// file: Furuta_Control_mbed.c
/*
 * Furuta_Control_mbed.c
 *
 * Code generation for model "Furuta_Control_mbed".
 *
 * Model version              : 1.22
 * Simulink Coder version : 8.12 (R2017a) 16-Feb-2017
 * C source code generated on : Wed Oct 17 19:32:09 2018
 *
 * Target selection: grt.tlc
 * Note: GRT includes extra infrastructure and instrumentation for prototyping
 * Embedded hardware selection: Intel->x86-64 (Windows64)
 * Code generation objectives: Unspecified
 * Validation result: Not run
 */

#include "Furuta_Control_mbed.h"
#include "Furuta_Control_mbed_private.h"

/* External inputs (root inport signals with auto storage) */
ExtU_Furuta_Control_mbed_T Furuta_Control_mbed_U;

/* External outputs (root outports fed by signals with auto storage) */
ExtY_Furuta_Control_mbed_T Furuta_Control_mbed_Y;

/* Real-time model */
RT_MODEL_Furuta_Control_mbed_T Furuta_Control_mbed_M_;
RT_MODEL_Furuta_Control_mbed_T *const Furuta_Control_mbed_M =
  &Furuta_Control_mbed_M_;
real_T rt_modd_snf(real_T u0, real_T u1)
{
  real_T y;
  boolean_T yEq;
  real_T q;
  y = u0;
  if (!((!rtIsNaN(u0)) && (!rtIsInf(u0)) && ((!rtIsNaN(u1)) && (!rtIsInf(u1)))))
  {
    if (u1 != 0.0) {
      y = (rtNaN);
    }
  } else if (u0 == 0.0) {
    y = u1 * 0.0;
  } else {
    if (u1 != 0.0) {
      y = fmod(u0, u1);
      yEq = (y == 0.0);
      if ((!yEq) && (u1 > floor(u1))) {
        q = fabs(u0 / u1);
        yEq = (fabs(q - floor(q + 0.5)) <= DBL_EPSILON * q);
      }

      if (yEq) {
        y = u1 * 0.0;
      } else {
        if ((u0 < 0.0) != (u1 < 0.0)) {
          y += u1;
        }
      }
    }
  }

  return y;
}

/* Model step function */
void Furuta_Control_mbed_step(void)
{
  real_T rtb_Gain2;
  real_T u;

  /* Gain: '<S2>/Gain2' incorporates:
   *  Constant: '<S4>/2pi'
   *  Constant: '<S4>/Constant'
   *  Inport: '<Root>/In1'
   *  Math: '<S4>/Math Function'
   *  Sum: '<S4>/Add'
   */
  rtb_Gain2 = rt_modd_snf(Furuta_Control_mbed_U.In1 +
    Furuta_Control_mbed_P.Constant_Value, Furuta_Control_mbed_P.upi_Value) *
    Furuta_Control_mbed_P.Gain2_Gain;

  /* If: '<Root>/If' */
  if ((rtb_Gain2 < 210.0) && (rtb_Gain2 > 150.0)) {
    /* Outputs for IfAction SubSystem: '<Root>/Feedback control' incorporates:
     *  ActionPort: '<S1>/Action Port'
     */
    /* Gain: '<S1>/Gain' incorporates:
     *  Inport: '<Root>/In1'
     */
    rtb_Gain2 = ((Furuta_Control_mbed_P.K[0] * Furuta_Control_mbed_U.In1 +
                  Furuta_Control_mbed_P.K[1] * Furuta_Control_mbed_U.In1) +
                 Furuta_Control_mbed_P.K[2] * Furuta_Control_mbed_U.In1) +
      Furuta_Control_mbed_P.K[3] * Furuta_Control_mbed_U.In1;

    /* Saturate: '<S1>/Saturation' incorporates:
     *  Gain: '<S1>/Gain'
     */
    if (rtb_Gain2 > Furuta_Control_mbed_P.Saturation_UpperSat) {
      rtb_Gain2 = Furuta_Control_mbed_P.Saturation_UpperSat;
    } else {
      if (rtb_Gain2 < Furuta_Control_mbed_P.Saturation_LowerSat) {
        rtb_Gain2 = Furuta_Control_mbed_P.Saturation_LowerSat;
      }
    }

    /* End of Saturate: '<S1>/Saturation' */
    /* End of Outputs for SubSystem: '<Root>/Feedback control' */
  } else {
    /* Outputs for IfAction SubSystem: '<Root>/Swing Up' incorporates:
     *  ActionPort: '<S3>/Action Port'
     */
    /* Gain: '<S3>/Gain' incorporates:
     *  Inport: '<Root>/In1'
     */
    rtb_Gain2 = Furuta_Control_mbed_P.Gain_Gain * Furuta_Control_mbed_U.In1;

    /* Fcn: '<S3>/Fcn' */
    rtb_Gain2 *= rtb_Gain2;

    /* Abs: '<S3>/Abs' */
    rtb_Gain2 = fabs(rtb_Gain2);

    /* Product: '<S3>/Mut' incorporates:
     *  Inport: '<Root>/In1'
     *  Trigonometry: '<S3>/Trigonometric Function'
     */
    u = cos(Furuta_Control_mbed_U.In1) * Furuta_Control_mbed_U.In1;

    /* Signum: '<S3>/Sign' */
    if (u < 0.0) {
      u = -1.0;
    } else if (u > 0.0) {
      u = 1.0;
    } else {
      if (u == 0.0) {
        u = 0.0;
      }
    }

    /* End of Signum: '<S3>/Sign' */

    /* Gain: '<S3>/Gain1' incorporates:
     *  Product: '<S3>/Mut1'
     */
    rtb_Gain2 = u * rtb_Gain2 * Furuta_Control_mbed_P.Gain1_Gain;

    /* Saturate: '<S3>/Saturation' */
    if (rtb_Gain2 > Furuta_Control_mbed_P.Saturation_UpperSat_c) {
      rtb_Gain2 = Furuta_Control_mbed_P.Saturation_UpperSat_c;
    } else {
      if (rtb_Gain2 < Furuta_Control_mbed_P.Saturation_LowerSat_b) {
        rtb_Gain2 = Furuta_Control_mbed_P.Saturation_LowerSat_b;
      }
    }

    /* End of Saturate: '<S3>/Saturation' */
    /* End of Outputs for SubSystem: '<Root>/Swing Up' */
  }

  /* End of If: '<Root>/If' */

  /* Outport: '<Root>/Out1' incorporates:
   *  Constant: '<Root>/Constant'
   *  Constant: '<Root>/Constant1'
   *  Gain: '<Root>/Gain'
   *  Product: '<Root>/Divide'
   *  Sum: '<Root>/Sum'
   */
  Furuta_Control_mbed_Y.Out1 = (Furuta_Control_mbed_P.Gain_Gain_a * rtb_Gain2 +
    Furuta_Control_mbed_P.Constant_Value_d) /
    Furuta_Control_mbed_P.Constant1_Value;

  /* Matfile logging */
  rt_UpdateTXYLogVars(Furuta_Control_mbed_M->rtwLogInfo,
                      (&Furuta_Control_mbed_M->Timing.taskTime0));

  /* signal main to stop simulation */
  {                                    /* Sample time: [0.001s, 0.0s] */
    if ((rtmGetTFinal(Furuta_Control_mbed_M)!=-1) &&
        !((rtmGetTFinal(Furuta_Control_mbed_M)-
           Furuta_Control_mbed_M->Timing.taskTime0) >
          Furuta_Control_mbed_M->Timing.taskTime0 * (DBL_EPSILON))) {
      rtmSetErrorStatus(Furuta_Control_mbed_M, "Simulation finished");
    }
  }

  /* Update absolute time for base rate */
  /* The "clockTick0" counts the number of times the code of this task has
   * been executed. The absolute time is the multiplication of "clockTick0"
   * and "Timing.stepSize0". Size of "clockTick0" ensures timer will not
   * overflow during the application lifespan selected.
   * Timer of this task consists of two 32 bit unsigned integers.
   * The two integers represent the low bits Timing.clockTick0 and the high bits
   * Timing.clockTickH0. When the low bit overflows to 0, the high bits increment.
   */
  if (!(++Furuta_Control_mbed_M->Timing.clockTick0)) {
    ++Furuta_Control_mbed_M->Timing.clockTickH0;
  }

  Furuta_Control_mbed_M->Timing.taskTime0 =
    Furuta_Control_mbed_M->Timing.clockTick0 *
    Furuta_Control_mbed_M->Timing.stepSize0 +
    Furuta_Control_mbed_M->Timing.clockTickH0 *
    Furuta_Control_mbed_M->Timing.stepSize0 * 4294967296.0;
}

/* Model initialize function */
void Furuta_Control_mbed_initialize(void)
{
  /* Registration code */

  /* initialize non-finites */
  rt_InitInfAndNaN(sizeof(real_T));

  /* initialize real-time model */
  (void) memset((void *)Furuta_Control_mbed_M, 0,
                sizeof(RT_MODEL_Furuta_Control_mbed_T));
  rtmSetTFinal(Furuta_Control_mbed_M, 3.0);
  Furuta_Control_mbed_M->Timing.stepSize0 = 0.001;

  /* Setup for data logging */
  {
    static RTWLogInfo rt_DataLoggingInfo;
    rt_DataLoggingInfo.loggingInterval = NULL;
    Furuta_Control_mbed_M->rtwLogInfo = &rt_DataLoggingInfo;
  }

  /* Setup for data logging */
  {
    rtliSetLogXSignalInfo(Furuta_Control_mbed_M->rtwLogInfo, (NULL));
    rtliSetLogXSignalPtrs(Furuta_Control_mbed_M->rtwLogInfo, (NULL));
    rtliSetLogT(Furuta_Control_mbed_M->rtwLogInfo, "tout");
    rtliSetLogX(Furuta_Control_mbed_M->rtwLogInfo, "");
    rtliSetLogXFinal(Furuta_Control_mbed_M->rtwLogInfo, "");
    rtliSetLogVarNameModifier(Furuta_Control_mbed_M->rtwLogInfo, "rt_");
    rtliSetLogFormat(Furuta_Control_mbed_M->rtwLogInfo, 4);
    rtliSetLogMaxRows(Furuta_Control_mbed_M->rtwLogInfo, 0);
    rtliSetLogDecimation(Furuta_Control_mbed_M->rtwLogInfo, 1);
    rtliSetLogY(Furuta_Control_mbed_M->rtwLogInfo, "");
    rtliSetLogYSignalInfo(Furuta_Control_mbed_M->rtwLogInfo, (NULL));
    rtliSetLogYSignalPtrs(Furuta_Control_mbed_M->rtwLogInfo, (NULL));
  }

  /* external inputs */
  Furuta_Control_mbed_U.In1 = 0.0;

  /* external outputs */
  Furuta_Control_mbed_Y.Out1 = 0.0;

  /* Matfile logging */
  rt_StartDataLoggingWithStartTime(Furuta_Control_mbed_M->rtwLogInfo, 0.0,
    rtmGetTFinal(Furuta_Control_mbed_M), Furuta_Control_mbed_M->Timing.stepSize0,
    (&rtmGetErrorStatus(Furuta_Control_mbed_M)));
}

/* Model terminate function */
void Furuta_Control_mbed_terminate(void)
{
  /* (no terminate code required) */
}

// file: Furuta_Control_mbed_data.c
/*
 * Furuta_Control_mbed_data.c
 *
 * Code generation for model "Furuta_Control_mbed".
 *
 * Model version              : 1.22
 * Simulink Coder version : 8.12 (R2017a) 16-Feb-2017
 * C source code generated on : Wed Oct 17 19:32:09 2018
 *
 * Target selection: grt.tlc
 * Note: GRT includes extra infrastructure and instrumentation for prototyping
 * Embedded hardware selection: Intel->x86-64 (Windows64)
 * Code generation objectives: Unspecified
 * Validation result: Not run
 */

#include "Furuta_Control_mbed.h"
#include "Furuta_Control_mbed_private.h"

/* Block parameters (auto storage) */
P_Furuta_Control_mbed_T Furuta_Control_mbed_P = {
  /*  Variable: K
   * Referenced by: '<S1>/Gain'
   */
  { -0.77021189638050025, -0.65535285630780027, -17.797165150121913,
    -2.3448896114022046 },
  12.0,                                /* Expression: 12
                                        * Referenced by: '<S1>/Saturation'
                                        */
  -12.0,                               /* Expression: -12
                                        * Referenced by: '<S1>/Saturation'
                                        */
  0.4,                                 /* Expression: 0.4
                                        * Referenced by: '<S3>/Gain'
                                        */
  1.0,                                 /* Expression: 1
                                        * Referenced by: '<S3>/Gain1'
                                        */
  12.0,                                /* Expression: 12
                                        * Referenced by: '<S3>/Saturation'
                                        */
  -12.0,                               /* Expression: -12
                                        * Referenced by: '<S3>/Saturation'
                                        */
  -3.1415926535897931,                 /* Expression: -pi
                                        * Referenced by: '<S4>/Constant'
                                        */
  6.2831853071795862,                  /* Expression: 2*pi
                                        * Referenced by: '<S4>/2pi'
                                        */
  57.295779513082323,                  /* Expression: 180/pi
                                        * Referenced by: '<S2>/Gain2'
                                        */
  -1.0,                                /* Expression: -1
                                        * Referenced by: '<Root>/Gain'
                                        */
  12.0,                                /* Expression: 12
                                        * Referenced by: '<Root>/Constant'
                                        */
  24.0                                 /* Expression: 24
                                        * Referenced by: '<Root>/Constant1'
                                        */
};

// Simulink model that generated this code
simulink model "Furuta_Control_mbed"  (R2017a)
settings: Solver=FixedStepDiscrete  StartTime=0.0  StopTime=3  FixedStep=Ts  RelTol=1e-3
PreLoadFcn:
  | %myBusDef
StartFcn:
  | % Full path to the block
  | %blk = 'Furuta_Control/Bus Creator';
  | 
  | % Attach the event listener
  | %h = add_exec_event_listener(blk, ...
  | %         'PostOutputs', @displayBusdata);
values from neighbouring files (symbols this model uses):
  K = Pxy*pinv(Pyy)    [UKF_RECURSIVE.m]    (also in example2.m = P12inv(P2); exemple_statler.m = Pxy/Pyy; exemple_statler2.m = Pxy/Pyy; ukf_teste.m = Pxy/Pyy)

== system Furuta_Control_mbed ==
  note: Transformation
  note: State FeedBack COntrol
  note: Input Signal
  In1 : Inport
  Constant : Constant  Value=12
  Constant1 : Constant  Value=24
  Demux : Demux
  Divide : Product  Inputs=*/
  Feedback control : Subsystem  TreatAsAtomicUnit=on
  Gain : Gain  Gain=-1
  If : If  IfExpression=(u1 < 210) & (u1 > 150)
  Merge : Merge
  Rad2Grad1 : Subsystem
  Sum : Sum  Inputs=|++
  Swing Up : Subsystem  TreatAsAtomicUnit=on
  Vector Concatenate3 : Concatenate  NumInputs=4
  Out1 : Outport
  wires:
  [State_FeedBack] -> Gain/1
  Vector Concatenate3/1 -> [State]
  If/2 -> Swing Up/Action
  [State] -> Feedback control/1(In1), Swing Up/1(In1)
  Swing Up/1(Out1) -> Merge/1
  Merge/1 -> [State_FeedBack]
  If/1 -> Feedback control/Action
  Rad2Grad1/1(ThetaGrad) -> If/1
  [Theta] -> Rad2Grad1/1(ThetaRad)
  Feedback control/1(Out1) -> Merge/2
  Gain/1 -> [Voltage]
  [Voltage] -> Sum/1
  Constant/1 -> Sum/2
  Sum/1 -> Divide/1
  Constant1/1 -> Divide/2
  Divide/1 -> Out1/1
  Demux/2 -> Vector Concatenate3/2
  Demux/3 -> [Theta], Vector Concatenate3/3
  Demux/4 -> Vector Concatenate3/4
  In1/1 -> Demux/1
  Demux/1 -> Vector Concatenate3/1

== system Furuta_Control_mbed/Feedback control ==
  In1 : Inport
  Action Port : ActionPort  ActionType=then
  Gain : Gain  Gain=K  Multiplication=Matrix(K*u)  ParamDataTypeStr=double  OutDataTypeStr=double
  Saturation : Saturate  UpperLimit=12  LowerLimit=-12
  Out1 : Outport
  wires:
  In1/1 -> Gain/1
  Gain/1 -> Saturation/1
  Saturation/1 -> Out1/1

== system Furuta_Control_mbed/Rad2Grad1 ==
  ThetaRad : Inport
  0-2pi : Subsystem
  Gain2 : Gain  Gain=180/pi
  ThetaGrad : Outport
  wires:
  ThetaRad/1 -> 0-2pi/1(In1)
  0-2pi/1(Out1) -> Gain2/1
  Gain2/1 -> ThetaGrad/1

== system Furuta_Control_mbed/Swing Up ==
  note: Swing-UP Control
  In1 : Inport
  Action Port : ActionPort  ActionType=else
  Abs : Abs
  Demux : Demux
  Fcn : Fcn  Expr=u(1)*u(1)
  Gain : Gain  Gain=0.4
  Gain1 : Gain
  Mut : Product  Inputs=**
  Mut1 : Product  Inputs=**
  Saturation : Saturate  UpperLimit=12  LowerLimit=-12
  Sign : Signum
  Terminator1 : Terminator
  Terminator2 : Terminator
  Trigonometric Function : Trigonometry  Operator=cos
  Out1 : Outport  InitialOutput=0
  wires:
  Saturation/1 -> Out1/1
  Demux/2 -> Terminator1/1
  Demux/1 -> Terminator2/1
  Gain1/1 -> Saturation/1
  Mut1/1 -> Gain1/1
  Demux/3 -> Trigonometric Function/1, Gain/1
  Fcn/1 -> Abs/1
  Trigonometric Function/1 -> Mut/1
  Demux/4 -> Mut/2
  Abs/1 -> Mut1/2
  Sign/1 -> Mut1/1
  Mut/1 -> Sign/1
  Gain/1 -> Fcn/1
  In1/1 -> Demux/1

== system Furuta_Control_mbed/Rad2Grad1/0-2pi ==
  In1 : Inport
  2pi : Constant  Value=2*pi
  Add : Sum
  Constant : Constant  Value=-pi
  Math Function : Math  Operator=mod  SaturateOnIntegerOverflow=on
  Out1 : Outport
  wires:
  Math Function/1 -> Out1/1
  2pi/1 -> Math Function/2
  Constant/1 -> Add/2
  In1/1 -> Add/1
  Add/1 -> Math Function/1
